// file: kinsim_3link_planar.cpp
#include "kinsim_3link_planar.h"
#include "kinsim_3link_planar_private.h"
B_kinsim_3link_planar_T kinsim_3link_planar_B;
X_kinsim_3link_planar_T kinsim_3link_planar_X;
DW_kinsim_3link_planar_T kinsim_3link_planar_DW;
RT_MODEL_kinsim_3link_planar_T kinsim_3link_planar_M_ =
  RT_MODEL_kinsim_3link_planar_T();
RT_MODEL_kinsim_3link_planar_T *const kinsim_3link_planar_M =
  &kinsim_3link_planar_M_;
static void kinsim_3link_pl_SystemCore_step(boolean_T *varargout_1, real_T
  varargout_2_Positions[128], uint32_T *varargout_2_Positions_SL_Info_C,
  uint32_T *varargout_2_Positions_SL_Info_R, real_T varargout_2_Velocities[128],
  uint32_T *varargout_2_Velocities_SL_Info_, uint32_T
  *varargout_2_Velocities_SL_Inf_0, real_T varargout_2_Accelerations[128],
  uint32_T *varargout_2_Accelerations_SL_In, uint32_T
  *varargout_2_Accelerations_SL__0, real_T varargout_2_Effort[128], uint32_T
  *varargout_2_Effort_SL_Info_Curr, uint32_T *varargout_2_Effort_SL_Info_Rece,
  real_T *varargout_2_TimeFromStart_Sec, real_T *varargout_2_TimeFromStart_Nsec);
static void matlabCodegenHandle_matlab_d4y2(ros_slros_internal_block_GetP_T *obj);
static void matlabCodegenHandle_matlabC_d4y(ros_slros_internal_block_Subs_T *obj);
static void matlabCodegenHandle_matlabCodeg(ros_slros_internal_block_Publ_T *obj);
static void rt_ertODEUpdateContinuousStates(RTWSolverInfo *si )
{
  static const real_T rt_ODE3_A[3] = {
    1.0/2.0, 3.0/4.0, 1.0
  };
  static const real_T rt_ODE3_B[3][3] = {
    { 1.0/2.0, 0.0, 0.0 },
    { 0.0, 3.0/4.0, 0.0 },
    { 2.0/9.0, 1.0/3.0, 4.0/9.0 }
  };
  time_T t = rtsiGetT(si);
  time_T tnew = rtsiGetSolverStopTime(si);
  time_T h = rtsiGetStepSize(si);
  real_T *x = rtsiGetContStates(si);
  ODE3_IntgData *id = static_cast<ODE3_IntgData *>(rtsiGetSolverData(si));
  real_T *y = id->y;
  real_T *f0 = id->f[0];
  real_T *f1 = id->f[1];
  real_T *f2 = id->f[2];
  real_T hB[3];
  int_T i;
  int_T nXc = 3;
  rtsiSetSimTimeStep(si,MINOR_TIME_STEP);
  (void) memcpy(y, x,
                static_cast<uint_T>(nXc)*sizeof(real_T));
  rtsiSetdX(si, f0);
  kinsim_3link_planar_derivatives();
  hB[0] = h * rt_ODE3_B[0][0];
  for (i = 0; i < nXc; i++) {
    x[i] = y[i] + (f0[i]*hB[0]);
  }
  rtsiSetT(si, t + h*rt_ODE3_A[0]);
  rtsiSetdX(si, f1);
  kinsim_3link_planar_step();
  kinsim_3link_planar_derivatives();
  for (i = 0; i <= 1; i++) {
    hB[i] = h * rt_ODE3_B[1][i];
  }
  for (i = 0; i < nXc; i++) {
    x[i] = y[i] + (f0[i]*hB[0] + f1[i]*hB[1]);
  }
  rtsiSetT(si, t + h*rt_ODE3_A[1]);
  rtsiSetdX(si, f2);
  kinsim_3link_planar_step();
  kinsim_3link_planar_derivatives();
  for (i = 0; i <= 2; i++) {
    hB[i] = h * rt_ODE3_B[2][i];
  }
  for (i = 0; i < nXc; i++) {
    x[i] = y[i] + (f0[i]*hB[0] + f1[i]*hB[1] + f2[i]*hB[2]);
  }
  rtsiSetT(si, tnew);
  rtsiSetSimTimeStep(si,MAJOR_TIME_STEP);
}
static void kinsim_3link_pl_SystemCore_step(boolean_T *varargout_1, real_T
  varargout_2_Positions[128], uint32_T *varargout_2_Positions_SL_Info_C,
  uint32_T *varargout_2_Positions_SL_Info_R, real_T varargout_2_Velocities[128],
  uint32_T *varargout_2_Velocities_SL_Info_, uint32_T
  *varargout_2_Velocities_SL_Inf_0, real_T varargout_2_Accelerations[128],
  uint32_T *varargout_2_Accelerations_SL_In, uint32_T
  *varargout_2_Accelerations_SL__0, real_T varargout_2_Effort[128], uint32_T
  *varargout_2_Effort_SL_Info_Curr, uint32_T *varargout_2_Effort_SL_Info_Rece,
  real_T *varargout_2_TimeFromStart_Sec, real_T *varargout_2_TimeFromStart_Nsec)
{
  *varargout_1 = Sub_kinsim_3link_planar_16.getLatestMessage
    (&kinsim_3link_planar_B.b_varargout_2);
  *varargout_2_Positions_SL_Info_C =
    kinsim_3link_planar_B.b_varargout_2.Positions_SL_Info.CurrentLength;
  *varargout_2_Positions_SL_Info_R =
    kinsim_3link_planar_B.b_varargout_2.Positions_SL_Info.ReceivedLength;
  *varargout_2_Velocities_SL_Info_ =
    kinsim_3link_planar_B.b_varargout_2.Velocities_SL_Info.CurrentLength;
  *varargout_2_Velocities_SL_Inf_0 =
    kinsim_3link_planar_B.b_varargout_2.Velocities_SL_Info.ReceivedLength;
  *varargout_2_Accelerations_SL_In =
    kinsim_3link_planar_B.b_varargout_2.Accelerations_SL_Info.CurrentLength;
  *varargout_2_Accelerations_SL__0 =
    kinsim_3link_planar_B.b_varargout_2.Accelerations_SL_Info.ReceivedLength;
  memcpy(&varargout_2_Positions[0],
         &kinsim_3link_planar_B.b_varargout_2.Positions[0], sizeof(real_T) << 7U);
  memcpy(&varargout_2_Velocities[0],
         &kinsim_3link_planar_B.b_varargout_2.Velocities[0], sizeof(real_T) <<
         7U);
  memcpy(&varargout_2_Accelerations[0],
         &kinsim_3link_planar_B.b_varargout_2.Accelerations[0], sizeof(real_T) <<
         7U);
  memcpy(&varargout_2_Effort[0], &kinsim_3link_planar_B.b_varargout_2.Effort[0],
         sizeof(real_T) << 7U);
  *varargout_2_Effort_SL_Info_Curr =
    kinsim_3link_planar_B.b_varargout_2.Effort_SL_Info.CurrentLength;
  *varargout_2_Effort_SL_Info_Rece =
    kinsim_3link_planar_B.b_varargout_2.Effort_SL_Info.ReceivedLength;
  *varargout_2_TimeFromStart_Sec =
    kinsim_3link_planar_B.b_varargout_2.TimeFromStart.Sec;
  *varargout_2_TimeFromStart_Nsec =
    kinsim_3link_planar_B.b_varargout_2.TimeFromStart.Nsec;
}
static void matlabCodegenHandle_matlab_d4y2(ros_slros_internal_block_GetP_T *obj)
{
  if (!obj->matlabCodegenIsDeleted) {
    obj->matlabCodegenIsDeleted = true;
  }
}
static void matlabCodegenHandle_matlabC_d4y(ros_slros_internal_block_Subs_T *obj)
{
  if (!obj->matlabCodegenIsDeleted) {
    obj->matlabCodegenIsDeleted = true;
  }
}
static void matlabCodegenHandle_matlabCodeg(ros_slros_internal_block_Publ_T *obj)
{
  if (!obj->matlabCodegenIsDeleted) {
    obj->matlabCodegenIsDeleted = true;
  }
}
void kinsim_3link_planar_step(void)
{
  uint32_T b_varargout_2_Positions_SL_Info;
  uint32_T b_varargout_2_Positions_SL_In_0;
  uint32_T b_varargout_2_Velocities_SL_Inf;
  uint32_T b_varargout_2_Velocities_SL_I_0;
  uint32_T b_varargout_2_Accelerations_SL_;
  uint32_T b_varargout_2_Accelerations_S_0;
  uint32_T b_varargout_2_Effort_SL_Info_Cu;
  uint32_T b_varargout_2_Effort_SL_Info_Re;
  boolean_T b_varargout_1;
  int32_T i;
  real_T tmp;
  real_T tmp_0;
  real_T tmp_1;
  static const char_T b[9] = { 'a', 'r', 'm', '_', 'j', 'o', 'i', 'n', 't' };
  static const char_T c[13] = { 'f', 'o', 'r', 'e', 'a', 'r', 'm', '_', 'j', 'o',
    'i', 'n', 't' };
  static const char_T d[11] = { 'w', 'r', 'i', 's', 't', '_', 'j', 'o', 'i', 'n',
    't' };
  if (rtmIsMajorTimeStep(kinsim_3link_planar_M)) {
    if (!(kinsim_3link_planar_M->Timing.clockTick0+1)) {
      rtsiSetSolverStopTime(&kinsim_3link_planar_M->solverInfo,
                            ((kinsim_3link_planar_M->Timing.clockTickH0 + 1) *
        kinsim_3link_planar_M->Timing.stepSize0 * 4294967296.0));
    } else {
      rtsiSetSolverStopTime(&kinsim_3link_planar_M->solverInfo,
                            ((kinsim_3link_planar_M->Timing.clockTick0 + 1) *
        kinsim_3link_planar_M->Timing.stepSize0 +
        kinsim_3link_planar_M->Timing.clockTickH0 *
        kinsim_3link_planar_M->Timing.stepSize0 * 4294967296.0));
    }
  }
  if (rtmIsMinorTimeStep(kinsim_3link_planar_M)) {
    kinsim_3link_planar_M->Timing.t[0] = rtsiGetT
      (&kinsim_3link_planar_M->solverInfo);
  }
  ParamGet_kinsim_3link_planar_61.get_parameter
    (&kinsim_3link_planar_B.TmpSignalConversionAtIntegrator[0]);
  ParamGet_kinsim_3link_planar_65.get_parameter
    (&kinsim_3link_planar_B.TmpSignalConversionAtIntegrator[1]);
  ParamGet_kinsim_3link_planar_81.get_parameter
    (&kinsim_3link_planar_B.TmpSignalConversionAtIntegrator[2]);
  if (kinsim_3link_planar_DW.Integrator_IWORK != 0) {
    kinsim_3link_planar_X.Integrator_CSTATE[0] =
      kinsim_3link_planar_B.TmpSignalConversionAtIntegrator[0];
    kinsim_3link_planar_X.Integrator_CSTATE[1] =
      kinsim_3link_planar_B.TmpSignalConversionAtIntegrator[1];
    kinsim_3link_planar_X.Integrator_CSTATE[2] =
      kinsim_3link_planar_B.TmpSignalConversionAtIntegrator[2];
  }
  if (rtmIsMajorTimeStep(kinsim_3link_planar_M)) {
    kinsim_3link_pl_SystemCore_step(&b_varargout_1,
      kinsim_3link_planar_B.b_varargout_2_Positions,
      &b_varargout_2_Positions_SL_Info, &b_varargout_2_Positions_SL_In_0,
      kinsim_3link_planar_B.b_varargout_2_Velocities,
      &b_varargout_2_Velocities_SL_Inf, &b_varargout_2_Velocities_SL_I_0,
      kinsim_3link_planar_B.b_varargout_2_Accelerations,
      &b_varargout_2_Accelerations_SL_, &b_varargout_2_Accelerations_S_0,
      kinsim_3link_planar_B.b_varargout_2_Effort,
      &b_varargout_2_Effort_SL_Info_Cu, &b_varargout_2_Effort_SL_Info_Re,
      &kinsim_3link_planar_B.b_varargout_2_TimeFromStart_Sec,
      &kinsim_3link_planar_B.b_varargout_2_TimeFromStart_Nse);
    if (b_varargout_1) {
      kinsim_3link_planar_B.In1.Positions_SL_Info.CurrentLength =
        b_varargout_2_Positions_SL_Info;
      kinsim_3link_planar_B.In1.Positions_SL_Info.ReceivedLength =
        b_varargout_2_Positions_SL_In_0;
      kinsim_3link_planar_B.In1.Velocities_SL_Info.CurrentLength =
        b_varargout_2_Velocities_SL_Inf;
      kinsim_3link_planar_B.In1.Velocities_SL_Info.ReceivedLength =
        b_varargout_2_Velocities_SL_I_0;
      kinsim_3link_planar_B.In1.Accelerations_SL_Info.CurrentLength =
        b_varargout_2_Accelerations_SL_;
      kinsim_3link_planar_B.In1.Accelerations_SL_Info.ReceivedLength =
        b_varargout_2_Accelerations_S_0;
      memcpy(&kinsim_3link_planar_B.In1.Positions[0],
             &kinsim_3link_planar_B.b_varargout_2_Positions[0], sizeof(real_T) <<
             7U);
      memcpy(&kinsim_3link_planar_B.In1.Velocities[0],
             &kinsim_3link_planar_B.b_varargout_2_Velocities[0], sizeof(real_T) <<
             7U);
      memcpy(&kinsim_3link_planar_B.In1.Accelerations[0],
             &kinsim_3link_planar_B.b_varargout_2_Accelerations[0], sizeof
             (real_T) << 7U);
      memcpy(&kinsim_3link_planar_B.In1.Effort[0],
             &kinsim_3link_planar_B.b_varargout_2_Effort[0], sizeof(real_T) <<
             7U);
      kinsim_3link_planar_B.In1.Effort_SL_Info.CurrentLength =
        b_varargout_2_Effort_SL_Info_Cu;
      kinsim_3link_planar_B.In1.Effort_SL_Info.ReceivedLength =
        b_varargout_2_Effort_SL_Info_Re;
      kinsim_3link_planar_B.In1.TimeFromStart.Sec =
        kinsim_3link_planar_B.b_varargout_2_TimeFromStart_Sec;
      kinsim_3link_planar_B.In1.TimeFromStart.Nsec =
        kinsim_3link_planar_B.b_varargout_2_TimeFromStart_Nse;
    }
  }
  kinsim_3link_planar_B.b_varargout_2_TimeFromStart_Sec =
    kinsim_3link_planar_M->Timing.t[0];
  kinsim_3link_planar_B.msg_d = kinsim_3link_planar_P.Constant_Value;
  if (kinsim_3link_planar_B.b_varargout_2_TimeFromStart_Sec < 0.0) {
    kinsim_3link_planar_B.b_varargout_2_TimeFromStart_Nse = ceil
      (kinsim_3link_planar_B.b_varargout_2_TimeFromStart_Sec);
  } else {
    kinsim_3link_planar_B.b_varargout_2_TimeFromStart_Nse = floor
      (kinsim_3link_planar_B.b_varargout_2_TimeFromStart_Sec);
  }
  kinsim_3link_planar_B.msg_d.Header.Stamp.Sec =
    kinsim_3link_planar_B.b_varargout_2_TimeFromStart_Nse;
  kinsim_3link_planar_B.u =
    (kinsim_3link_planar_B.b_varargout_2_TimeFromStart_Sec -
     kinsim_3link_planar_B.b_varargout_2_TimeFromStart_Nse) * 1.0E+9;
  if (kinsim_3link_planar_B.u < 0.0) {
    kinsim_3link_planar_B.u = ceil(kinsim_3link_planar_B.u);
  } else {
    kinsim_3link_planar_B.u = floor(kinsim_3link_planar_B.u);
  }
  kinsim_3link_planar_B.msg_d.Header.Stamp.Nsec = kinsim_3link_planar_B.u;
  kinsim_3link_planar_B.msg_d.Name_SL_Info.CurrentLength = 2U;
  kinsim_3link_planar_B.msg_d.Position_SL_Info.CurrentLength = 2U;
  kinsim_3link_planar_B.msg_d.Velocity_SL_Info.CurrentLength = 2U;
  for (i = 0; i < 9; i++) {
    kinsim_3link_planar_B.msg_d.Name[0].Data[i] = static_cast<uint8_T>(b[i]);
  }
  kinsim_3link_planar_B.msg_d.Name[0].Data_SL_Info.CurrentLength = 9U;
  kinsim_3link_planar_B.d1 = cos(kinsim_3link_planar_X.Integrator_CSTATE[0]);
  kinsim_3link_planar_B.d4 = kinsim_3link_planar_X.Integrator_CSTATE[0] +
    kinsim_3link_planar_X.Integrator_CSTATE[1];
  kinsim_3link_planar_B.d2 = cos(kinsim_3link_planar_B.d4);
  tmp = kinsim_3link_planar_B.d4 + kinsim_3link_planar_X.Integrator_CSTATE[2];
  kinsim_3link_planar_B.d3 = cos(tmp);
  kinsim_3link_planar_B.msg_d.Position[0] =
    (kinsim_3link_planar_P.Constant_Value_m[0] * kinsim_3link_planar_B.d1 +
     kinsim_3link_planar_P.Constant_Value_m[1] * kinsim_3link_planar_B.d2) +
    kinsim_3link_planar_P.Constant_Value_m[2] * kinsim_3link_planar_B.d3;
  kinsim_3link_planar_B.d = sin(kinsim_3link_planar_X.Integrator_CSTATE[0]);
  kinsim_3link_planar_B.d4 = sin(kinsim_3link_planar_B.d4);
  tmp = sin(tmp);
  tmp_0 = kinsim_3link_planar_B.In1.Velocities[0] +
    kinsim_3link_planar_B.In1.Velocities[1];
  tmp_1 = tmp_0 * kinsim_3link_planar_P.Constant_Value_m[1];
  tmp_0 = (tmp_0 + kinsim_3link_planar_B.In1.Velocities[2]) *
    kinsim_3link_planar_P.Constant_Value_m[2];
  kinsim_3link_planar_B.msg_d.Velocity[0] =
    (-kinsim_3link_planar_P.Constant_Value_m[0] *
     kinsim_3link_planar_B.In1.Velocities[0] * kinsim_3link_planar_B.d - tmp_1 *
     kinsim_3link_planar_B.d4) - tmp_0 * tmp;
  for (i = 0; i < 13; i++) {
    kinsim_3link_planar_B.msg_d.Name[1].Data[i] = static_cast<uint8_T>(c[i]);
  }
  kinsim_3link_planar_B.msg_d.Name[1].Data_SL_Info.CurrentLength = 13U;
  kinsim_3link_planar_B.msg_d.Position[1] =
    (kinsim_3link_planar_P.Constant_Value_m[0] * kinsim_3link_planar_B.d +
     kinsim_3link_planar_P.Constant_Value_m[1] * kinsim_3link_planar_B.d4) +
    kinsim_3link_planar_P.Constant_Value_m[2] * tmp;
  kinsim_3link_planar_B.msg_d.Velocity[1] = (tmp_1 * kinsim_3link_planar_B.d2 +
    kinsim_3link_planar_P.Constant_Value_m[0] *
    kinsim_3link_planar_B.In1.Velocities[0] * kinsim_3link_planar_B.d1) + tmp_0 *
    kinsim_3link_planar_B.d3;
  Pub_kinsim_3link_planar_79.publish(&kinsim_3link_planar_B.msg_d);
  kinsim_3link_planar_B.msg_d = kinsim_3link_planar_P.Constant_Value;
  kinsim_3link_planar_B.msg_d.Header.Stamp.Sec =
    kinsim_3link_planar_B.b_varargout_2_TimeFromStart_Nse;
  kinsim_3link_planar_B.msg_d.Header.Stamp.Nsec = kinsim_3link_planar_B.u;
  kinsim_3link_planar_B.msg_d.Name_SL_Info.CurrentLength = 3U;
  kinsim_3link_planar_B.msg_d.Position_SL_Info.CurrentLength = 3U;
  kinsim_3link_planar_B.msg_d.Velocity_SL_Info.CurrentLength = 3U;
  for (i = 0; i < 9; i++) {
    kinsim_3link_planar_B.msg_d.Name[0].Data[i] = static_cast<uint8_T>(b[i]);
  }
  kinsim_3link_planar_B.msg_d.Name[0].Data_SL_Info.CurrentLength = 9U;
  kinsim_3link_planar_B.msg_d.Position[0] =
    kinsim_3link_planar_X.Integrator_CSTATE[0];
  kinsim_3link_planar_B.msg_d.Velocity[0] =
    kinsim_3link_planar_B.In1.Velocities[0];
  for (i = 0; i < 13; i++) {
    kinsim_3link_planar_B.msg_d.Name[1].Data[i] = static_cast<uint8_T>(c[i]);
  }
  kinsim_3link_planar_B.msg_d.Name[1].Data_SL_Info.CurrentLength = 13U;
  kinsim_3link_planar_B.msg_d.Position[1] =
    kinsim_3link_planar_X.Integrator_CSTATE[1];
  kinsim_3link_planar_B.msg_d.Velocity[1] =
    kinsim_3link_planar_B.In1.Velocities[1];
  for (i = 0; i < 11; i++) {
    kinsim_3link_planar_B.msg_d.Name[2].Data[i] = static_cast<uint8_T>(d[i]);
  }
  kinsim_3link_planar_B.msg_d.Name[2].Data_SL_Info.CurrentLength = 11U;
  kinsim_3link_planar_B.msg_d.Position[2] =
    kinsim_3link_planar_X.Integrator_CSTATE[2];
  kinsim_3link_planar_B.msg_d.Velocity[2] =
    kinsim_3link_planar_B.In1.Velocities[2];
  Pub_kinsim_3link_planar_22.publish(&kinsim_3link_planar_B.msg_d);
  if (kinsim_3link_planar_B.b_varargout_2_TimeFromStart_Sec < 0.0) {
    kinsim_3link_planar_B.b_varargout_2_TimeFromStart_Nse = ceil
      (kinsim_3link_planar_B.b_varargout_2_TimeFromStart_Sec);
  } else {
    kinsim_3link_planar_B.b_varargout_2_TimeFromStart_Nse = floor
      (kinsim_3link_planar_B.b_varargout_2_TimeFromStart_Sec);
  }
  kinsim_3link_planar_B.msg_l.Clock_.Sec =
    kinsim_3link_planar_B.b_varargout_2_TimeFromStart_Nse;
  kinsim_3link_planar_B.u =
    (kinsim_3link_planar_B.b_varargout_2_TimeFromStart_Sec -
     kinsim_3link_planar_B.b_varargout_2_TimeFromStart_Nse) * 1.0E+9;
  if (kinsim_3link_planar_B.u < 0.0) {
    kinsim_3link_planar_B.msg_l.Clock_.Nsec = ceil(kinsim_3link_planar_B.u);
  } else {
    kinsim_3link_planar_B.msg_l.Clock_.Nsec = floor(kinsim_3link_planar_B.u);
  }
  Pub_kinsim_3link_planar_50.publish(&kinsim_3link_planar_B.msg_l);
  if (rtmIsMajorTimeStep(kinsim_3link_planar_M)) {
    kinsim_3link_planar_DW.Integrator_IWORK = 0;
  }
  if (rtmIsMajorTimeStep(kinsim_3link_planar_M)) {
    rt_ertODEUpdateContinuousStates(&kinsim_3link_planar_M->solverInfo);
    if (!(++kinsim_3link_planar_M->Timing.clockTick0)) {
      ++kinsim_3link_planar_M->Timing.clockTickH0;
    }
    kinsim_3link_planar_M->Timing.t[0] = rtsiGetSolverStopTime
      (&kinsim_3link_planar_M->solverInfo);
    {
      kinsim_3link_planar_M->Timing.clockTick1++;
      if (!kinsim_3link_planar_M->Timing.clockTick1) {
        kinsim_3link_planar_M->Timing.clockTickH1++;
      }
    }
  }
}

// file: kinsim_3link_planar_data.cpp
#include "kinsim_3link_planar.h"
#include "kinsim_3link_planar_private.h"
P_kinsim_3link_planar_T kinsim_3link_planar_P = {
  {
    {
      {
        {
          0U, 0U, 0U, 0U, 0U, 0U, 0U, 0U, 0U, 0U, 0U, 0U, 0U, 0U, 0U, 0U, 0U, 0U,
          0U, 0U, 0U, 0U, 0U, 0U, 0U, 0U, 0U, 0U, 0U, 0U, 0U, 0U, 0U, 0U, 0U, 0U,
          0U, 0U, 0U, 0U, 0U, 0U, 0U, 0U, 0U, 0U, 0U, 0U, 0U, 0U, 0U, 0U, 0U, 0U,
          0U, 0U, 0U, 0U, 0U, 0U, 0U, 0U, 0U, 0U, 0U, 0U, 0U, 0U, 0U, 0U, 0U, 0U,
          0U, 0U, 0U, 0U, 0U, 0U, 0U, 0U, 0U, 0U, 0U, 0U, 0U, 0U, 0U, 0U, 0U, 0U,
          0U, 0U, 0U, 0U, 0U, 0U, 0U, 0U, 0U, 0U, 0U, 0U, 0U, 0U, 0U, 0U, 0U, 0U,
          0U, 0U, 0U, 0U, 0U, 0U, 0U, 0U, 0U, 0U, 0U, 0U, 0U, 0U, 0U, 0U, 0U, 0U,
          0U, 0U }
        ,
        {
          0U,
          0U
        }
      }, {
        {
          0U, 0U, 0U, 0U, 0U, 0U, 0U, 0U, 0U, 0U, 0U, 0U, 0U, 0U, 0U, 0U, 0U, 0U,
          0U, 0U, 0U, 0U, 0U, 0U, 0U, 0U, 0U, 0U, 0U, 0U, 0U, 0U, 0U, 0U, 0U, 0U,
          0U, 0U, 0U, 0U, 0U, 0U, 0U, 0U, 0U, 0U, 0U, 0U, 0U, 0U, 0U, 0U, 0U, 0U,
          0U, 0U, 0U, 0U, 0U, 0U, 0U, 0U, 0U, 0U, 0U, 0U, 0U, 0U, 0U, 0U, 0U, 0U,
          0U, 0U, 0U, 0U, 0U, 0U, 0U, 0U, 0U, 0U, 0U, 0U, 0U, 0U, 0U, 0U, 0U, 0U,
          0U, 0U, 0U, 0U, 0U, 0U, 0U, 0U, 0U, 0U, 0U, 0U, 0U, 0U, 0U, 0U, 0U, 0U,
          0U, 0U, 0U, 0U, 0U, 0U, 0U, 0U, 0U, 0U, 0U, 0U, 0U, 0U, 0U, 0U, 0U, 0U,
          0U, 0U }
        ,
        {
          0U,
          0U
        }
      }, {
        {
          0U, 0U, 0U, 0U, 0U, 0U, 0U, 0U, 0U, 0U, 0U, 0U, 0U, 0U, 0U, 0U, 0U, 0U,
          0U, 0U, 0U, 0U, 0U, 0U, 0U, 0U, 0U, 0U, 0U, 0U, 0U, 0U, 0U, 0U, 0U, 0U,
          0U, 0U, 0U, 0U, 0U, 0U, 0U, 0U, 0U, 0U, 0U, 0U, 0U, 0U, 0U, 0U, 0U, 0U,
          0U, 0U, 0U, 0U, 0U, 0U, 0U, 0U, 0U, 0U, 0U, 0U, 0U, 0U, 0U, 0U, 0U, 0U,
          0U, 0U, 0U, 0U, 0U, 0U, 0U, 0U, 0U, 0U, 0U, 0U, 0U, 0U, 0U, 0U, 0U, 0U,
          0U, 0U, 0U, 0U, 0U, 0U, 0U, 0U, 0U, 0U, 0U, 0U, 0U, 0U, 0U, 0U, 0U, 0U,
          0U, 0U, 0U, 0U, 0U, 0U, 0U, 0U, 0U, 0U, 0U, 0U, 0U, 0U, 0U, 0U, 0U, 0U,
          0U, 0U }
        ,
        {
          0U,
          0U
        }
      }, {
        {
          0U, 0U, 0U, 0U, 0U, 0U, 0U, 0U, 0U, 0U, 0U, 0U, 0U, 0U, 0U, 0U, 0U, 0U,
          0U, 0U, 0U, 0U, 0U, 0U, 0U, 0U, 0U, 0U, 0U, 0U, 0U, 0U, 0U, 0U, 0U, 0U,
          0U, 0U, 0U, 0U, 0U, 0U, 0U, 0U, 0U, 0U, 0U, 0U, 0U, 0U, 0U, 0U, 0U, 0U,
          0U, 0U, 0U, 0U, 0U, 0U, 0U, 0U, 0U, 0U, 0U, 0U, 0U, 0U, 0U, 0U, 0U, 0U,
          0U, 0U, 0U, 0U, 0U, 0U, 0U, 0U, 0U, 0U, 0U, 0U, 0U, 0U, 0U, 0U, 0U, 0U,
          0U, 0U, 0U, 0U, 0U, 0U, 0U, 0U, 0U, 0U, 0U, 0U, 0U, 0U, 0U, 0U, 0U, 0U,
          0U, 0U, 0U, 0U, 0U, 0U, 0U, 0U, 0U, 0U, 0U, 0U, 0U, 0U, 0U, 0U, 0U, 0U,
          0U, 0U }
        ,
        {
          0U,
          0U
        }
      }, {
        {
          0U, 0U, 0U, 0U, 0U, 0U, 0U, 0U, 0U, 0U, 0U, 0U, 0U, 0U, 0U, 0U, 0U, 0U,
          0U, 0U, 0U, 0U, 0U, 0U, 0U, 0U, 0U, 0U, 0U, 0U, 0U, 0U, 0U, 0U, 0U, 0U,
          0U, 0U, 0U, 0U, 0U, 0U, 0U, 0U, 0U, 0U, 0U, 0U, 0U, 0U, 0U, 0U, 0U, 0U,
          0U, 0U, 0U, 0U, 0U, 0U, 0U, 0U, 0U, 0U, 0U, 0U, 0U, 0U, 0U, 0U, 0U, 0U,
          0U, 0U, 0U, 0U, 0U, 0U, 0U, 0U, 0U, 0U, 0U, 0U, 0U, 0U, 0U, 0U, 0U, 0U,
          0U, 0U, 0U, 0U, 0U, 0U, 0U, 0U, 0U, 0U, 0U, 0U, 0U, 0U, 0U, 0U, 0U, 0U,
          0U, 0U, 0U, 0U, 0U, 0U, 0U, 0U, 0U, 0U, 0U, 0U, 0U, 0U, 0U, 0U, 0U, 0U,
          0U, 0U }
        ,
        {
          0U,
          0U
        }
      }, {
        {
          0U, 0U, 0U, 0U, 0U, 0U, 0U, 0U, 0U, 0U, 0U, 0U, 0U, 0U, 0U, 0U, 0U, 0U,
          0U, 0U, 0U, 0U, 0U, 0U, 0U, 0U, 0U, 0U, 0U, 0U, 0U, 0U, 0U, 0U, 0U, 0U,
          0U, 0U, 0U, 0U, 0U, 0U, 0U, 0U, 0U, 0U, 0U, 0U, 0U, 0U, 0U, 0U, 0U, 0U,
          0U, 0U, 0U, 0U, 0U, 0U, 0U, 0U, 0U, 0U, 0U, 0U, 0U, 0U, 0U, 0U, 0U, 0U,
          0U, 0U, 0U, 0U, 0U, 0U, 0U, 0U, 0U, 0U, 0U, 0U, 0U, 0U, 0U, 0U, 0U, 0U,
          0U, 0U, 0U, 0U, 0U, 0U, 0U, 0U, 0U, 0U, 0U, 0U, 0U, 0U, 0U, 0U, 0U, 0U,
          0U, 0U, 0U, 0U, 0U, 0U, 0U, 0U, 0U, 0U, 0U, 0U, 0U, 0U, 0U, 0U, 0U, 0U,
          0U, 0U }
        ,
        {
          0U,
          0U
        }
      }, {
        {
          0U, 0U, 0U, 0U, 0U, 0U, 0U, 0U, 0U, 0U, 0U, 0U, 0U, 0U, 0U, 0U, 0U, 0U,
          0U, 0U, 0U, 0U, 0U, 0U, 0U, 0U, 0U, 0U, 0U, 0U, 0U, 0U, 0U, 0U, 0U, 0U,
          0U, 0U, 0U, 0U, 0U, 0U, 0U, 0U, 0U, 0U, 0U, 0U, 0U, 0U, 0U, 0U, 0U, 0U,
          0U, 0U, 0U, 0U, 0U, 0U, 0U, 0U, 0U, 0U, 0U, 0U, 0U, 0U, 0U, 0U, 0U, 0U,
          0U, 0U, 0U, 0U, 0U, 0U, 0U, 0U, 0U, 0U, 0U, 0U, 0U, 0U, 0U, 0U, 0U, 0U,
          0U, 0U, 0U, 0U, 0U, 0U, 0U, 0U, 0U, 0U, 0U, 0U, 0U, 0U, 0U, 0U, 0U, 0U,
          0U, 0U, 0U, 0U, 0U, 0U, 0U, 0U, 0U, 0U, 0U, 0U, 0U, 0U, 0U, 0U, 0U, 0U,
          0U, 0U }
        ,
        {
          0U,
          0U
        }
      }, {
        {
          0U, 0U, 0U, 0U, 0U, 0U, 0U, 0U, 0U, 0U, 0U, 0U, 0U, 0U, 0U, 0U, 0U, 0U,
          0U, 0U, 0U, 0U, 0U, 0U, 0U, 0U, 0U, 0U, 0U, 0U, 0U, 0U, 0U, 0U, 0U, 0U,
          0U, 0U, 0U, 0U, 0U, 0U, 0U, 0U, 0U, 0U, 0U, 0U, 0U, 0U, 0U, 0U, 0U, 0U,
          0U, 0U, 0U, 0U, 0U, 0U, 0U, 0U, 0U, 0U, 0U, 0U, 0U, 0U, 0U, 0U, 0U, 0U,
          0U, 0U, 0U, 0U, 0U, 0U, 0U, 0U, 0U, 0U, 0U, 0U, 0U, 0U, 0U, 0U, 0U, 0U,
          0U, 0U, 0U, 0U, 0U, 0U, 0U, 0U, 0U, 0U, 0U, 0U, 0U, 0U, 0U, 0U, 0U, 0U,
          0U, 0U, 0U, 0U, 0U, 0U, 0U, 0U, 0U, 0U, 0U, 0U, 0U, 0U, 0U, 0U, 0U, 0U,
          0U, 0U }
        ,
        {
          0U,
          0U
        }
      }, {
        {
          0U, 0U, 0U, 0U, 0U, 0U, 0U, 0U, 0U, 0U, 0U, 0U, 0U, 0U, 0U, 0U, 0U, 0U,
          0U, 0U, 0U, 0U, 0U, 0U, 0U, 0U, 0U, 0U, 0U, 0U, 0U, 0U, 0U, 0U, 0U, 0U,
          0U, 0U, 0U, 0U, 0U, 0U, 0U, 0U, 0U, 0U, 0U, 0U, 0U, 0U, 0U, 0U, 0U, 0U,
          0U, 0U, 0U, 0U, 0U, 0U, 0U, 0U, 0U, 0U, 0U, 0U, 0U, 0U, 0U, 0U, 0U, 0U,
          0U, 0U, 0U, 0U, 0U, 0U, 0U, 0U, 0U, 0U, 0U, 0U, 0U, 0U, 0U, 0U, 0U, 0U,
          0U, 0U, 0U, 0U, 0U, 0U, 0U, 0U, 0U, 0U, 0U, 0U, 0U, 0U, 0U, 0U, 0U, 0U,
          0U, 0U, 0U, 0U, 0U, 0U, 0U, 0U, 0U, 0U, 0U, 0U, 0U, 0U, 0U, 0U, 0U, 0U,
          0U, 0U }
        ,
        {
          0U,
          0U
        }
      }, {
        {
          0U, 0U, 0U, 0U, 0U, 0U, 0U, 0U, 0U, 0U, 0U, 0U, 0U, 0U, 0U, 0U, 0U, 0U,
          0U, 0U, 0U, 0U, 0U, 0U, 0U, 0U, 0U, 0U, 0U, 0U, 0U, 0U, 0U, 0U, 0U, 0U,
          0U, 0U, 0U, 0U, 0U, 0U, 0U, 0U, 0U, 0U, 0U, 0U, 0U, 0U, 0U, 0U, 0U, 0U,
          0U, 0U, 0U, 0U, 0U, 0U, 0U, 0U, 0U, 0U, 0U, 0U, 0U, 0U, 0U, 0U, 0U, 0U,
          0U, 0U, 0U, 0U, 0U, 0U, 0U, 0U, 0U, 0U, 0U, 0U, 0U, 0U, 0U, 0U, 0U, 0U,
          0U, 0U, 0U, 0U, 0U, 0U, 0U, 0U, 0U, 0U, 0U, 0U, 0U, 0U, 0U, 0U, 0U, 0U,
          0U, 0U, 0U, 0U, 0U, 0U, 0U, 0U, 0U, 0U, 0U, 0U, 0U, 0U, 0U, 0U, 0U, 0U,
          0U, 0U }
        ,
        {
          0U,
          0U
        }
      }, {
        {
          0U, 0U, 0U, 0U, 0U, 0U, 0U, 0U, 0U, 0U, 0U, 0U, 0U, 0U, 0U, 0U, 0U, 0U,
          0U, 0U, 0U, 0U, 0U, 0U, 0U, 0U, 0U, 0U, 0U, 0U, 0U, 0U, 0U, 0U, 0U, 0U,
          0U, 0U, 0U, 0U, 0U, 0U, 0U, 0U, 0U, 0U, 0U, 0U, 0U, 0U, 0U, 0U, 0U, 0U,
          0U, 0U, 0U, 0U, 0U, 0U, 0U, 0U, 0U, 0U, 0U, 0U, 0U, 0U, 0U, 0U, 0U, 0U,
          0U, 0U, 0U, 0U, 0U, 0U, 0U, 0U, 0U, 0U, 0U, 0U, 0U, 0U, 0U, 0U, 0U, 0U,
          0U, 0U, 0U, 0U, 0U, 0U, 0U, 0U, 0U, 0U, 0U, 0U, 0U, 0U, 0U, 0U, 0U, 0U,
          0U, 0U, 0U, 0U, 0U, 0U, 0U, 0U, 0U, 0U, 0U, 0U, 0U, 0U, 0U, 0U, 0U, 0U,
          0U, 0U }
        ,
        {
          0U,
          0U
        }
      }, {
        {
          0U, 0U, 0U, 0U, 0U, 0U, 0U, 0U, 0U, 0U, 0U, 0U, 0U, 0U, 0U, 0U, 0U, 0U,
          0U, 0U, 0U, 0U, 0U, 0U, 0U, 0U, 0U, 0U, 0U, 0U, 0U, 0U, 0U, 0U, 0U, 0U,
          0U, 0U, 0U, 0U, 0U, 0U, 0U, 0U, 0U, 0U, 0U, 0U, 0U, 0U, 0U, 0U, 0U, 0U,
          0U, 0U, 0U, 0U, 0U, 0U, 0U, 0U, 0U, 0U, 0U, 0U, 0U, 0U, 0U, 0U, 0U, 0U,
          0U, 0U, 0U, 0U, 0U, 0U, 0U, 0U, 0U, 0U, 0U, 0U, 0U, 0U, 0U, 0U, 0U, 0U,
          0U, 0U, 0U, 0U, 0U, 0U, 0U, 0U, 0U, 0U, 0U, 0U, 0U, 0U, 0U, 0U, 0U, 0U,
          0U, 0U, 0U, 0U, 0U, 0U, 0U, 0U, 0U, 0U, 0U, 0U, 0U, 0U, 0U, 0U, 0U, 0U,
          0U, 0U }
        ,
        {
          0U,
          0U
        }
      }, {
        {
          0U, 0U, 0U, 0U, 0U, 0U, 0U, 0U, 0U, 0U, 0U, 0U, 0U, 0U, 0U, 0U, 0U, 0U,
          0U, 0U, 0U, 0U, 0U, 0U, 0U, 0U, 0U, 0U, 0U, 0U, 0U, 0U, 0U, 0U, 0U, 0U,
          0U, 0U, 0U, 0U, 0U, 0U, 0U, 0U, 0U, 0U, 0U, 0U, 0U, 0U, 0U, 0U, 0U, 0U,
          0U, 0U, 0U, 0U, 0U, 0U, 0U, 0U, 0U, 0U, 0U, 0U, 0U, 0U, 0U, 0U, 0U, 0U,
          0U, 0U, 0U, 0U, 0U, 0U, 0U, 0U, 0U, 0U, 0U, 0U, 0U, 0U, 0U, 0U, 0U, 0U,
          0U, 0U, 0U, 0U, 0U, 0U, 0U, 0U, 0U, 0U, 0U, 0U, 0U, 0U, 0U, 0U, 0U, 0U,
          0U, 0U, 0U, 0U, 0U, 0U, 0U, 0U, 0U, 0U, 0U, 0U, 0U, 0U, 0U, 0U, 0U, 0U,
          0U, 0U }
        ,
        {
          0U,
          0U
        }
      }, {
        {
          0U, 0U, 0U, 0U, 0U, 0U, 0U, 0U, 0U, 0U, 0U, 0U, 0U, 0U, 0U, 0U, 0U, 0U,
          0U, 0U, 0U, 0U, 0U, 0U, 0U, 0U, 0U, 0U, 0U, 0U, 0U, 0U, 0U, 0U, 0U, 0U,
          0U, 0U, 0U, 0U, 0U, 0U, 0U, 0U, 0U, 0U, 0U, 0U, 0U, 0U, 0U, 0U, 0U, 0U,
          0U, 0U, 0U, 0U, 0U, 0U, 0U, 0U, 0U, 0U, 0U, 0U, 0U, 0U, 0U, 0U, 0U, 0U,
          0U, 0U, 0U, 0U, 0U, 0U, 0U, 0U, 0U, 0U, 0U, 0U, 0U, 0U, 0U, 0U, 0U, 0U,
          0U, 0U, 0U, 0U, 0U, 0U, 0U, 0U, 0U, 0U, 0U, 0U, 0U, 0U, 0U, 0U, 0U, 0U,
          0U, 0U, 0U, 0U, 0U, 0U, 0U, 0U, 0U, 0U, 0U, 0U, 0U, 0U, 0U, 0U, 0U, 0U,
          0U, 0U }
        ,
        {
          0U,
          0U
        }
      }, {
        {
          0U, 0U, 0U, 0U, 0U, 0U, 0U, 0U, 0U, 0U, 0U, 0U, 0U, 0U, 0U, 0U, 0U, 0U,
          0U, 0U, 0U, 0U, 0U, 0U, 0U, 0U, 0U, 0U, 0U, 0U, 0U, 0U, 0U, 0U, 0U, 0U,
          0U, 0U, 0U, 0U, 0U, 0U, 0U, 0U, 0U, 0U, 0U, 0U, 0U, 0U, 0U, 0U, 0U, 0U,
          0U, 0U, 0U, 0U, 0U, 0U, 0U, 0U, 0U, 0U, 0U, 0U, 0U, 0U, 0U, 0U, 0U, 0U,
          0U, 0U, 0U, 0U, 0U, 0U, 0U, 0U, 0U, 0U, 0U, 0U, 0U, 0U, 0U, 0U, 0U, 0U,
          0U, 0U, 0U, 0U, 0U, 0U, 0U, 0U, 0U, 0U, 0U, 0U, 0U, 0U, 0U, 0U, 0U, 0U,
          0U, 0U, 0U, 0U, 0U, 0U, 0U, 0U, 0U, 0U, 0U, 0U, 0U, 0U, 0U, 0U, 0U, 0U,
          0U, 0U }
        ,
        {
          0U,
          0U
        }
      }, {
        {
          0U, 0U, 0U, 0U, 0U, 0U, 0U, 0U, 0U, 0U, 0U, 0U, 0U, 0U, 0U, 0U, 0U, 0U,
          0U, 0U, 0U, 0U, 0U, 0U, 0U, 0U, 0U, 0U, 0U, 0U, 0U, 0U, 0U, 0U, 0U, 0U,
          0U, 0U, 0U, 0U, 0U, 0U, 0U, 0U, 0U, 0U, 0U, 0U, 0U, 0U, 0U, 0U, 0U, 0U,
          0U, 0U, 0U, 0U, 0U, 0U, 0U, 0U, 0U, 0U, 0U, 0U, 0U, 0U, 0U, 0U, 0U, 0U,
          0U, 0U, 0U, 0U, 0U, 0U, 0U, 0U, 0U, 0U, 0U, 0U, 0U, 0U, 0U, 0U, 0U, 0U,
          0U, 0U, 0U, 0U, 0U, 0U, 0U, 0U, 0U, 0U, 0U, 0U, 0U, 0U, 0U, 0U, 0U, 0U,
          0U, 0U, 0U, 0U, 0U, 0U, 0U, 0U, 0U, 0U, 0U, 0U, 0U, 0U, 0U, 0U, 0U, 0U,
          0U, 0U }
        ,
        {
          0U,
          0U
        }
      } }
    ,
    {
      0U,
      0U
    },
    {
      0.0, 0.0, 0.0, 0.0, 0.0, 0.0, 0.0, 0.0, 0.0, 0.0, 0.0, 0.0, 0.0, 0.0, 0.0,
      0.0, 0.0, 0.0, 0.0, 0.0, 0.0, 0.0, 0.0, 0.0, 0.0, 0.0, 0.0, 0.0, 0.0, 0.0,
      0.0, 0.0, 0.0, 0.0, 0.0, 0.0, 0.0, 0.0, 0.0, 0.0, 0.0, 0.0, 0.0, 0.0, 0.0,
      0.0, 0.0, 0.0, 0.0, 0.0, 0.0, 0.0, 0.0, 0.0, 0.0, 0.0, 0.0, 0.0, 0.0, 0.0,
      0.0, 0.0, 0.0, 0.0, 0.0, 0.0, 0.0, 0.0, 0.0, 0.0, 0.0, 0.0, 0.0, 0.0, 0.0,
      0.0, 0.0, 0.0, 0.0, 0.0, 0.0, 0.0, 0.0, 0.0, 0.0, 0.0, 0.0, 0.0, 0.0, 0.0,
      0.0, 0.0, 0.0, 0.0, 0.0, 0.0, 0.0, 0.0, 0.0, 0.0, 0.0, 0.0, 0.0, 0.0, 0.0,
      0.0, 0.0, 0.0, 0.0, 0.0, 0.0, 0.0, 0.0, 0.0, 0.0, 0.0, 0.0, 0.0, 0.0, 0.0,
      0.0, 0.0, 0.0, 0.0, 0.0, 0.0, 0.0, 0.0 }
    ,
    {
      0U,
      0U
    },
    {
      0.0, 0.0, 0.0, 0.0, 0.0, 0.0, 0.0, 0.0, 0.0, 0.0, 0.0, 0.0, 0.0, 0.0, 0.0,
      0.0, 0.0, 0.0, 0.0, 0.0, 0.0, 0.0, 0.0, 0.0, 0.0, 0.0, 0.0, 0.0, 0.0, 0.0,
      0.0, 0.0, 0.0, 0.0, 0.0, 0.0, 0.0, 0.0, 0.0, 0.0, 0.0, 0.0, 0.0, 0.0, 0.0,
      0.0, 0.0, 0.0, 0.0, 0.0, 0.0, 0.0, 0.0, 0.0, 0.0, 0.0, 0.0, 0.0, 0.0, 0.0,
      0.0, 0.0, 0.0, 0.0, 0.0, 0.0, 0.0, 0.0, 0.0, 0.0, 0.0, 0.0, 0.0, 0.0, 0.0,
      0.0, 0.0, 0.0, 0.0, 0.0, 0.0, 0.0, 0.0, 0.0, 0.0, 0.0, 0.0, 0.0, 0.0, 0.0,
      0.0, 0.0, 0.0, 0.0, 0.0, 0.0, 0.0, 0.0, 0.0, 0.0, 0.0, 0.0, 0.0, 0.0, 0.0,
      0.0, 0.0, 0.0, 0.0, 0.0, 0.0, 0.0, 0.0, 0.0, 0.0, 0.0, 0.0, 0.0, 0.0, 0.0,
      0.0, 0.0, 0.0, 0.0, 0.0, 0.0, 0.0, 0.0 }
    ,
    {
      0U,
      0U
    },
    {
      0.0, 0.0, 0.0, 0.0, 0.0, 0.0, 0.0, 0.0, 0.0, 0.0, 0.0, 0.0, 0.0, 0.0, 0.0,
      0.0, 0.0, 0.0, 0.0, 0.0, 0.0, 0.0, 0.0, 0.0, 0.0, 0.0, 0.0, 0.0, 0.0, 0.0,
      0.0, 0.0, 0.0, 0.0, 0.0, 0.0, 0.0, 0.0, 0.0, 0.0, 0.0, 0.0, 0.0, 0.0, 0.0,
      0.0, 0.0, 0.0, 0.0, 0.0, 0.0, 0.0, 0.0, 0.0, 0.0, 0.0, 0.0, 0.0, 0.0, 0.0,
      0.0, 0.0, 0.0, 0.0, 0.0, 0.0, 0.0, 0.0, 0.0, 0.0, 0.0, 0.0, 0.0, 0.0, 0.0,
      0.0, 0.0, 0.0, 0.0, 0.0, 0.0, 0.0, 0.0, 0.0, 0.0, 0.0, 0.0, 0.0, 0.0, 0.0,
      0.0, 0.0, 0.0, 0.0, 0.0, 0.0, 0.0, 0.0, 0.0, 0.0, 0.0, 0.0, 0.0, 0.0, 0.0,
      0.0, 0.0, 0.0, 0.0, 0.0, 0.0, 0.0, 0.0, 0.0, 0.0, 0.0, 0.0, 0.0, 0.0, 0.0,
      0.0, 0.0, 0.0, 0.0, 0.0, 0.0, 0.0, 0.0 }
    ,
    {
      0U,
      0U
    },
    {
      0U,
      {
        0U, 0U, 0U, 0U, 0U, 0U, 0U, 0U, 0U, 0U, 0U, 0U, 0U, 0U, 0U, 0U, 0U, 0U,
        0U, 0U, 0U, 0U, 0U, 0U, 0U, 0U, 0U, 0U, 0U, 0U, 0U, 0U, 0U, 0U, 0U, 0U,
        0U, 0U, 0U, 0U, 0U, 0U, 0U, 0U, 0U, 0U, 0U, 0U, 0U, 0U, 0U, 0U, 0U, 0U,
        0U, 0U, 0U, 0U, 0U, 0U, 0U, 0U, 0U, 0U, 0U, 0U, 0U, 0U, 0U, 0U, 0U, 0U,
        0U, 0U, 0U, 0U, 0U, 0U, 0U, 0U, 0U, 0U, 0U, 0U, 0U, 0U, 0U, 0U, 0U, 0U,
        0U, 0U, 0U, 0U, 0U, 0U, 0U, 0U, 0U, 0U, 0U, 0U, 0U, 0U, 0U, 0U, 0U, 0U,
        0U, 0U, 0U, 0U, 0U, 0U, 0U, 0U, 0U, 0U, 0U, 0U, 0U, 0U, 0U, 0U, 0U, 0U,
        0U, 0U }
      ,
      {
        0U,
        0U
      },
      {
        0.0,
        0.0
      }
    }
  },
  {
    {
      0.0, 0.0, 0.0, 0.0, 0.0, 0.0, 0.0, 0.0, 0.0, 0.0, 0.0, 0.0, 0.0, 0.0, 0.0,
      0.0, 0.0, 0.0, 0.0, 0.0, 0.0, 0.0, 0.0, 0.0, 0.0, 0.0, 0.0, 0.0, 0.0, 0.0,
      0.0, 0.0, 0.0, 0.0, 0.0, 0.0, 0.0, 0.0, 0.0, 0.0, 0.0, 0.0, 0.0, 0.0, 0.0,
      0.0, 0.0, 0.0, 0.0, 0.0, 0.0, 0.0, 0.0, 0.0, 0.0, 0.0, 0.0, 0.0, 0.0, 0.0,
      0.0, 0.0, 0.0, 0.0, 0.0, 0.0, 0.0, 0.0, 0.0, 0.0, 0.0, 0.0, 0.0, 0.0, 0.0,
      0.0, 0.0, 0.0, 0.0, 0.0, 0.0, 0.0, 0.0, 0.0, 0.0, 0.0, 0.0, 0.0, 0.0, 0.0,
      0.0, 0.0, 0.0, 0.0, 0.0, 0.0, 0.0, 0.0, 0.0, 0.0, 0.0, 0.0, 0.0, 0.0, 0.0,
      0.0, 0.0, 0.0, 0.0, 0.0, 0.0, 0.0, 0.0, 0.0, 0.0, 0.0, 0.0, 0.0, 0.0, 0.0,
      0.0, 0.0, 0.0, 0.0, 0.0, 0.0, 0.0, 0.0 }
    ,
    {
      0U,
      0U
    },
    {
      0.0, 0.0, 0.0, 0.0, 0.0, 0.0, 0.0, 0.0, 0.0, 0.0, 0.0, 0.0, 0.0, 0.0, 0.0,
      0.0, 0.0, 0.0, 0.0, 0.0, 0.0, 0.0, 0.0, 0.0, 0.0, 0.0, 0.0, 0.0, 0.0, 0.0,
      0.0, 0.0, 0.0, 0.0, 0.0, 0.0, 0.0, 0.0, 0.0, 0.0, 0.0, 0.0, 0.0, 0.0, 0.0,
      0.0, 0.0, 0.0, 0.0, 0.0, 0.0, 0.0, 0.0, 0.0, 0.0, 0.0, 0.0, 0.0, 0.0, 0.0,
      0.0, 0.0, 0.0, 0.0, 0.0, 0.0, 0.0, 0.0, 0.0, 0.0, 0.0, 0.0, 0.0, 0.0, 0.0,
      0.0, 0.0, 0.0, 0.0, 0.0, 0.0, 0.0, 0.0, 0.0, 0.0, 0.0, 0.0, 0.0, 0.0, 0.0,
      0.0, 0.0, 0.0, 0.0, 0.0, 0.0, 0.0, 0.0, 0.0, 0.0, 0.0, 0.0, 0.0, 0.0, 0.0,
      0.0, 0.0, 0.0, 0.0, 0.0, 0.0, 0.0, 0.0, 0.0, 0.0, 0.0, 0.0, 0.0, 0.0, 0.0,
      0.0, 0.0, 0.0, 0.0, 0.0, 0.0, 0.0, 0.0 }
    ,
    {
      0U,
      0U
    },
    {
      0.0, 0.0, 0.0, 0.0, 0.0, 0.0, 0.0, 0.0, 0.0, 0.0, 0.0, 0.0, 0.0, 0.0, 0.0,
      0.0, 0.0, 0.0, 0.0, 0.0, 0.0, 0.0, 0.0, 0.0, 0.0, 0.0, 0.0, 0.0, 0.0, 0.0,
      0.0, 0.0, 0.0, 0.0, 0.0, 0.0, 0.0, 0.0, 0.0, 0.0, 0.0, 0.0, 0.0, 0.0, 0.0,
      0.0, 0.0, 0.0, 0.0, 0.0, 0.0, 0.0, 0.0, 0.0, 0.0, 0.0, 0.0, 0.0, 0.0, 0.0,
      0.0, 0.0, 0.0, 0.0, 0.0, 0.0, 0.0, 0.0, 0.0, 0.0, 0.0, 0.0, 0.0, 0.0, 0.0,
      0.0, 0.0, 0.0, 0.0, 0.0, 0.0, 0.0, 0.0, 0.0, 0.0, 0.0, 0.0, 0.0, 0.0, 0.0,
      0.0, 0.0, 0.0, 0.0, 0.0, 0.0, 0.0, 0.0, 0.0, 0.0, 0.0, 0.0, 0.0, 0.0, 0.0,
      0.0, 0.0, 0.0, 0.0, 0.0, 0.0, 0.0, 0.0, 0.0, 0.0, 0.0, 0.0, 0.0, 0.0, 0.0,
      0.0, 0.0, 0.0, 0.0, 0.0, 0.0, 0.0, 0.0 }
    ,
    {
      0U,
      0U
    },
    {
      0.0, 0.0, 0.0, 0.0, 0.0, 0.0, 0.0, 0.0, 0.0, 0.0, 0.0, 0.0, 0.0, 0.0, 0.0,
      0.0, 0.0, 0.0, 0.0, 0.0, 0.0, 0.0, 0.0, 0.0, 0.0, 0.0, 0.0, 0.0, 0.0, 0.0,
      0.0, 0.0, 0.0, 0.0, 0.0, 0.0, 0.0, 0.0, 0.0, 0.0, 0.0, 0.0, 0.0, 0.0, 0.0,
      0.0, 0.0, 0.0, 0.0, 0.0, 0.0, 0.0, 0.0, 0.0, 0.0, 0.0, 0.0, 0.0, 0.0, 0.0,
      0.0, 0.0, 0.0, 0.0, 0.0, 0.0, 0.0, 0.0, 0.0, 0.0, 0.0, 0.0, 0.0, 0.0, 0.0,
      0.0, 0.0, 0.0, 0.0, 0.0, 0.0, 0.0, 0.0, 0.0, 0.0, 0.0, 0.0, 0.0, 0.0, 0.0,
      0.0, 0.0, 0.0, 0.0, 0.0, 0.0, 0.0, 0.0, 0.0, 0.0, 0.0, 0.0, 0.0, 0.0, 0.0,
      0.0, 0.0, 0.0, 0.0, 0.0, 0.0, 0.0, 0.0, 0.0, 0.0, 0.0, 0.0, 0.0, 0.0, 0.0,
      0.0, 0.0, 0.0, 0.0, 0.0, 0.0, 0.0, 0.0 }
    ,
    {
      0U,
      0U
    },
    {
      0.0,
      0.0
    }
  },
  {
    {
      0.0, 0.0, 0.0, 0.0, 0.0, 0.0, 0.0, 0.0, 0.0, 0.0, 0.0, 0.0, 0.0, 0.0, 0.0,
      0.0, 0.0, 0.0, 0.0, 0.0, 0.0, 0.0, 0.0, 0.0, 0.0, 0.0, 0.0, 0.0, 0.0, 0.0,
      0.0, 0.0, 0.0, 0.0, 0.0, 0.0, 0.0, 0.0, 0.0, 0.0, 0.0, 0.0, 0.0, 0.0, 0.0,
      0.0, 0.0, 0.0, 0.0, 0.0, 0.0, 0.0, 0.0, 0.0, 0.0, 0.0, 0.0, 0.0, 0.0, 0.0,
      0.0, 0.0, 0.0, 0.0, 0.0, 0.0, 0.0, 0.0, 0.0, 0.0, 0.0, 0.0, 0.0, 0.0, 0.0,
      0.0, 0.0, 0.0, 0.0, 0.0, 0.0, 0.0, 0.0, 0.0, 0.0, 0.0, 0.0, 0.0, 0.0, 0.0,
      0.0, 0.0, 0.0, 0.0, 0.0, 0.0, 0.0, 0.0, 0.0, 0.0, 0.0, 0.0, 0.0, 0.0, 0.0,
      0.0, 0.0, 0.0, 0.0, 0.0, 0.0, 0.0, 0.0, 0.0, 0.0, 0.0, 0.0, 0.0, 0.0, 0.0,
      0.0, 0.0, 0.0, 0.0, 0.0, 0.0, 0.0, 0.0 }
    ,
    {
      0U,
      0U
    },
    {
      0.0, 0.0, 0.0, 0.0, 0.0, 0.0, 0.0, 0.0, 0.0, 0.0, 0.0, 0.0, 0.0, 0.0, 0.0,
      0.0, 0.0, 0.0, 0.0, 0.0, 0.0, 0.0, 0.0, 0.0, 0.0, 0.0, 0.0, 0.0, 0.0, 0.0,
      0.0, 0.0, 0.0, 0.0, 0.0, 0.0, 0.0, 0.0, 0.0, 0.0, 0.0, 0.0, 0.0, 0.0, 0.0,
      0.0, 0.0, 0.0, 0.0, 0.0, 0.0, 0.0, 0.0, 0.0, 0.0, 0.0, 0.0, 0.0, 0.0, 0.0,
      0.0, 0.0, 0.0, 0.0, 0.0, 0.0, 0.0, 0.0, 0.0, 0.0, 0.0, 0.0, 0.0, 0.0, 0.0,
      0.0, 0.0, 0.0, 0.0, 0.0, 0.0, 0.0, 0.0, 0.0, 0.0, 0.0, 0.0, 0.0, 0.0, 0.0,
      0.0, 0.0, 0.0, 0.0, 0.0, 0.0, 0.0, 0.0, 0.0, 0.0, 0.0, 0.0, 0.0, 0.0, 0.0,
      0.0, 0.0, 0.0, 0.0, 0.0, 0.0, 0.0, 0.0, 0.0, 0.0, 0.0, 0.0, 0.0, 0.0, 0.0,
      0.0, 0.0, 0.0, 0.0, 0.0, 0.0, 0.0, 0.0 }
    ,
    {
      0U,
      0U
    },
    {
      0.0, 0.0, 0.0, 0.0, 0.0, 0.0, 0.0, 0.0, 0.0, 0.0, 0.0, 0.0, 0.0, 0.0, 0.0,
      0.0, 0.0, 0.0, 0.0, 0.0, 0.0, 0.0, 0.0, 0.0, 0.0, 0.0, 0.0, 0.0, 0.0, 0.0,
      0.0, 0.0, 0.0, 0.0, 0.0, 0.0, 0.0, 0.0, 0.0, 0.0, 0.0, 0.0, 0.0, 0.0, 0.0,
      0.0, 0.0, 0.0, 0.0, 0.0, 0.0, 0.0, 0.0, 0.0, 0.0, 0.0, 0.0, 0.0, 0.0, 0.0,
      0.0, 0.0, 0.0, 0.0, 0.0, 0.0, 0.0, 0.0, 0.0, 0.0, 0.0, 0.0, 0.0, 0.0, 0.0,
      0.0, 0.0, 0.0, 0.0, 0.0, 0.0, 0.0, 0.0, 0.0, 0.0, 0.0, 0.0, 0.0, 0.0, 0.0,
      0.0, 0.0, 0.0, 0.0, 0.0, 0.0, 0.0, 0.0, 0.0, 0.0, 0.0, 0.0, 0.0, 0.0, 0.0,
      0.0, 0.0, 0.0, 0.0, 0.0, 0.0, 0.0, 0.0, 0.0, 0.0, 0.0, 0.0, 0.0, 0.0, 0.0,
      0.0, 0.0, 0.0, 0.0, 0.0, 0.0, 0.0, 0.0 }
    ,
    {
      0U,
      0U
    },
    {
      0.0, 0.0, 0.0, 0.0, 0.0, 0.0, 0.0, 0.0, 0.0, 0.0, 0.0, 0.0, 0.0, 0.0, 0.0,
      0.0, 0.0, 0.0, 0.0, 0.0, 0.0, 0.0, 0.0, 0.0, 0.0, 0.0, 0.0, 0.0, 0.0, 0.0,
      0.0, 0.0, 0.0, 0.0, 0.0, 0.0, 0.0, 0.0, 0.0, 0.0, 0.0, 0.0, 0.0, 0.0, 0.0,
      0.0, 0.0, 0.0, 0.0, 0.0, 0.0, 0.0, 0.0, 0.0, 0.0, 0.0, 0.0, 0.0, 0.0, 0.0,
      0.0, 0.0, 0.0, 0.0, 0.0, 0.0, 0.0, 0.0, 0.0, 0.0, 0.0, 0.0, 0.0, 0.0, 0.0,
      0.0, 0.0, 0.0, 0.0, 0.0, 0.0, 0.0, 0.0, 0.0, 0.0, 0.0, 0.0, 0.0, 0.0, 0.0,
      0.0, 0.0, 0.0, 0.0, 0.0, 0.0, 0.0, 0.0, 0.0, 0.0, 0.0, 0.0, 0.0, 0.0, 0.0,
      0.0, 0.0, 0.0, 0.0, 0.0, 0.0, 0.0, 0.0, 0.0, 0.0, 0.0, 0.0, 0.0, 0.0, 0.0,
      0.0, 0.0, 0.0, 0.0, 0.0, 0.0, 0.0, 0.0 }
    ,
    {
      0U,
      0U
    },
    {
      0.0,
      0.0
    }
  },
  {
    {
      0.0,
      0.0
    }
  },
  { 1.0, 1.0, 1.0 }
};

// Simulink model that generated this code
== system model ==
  Publish#1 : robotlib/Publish  <- 1: MATLABFunction#1
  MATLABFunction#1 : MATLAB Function  <- 1: BlankMessage#1, 2: MATLABFunction#2, 3: MATLABFunction#2/2, 4: Clock#1
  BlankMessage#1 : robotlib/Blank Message
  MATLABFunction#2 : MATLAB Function  <- 1: Integrator, 2: Selector#1, 3: Constant
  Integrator : Integrator  InitialCondition=[0,0]  <- 1: Selector#1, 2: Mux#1
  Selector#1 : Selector  Indices=[1]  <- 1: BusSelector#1
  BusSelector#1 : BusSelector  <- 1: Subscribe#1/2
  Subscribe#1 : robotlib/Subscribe
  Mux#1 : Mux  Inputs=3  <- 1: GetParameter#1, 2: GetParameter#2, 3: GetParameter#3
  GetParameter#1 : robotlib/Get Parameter
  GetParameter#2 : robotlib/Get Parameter
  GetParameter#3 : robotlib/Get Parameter
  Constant : Constant  Value=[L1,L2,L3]
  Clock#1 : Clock
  Publish#2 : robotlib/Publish  <- 1: MATLABFunction#3
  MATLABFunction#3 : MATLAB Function  <- 1: BlankMessage#1, 2: Integrator, 3: Selector#1, 4: Clock#1
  Publish#3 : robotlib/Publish  <- 1: MATLABFunction#4
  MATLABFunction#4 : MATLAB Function  <- 1: BlankMessage#2, 2: Clock
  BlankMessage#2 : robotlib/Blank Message
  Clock : Clock
== matlab function MATLABFunction#4 ==
function msg = assign_Time(blankMessage,time)
%#codegen

% Assign the output message to be the same with input blank message
msg = blankMessage;

% Convert and set time
msg.Clock_.Sec  = fix(time);
msg.Clock_.Nsec = fix((time-fix(time))*1e9);

== matlab function MATLABFunction#3 ==
function msg = assign_JointState(blankMessage,jointPos,jointVel,time)
%#codegen

% Assign the output message to be the same with input blank message
msg = blankMessage;

% Initialize time stamp
msg.Header.Stamp.Sec  = fix(time);
msg.Header.Stamp.Nsec = fix((time-fix(time))*1e9);

% Set the number of strings in the string array, and joint positions/velocities in the position/velocity array
numJoints = length(jointPos);
msg.Name_SL_Info.CurrentLength = uint32(numJoints);
msg.Position_SL_Info.CurrentLength = uint32(numJoints);
msg.Velocity_SL_Info.CurrentLength = uint32(numJoints);

% Set the individual components in the message arrays
strArrayToAssign = {'arm_joint', 'forearm_joint', 'wrist_joint'};

for idx=1:numJoints
    str = strArrayToAssign{idx};
    strLength = length(str);
    msg.Name(idx).Data(1:strLength) = uint8(str);
    msg.Name(idx).Data_SL_Info.CurrentLength = uint32(strLength);

    msg.Position(idx) = jointPos(idx);
    msg.Velocity(idx) = jointVel(idx);
end

== matlab function MATLABFunction#2 ==
function [cartPos, cartVel] = forward_kinematics_3link(jointPos,jointVel,linkLength)

cartPos = zeros(1,2);
cartVel = zeros(1,2);

L1 = linkLength(1);
L2 = linkLength(2);
L3 = linkLength(3);
q1 = jointPos(1);
q2 = jointPos(2);
q3 = jointPos(3);
qv1 = jointVel(1);
qv2 = jointVel(2);
qv3 = jointVel(3);

cartPos(1) = L1*cos(q1)+L2*cos(q1+q2)+L3*cos(q1+q2+q3);
cartPos(2) = L1*sin(q1)+L2*sin(q1+q2)+L3*sin(q1+q2+q3);
cartVel(1) = -L1*qv1*sin(q1)-L2*(qv1+qv2)*sin(q1+q2)-L3*(qv1+qv2+qv3)*sin(q1+q2+q3);
cartVel(2) = L1*qv1*cos(q1)+L2*(qv1+qv2)*cos(q1+q2)+L3*(qv1+qv2+qv3)*cos(q1+q2+q3);

== matlab function MATLABFunction#1 ==
function msg = assign_CartesianState(blankMessage,cartPos,cartVel,time)
%#codegen

% Assign the output message to be the same with input blank message
msg = blankMessage;

% Initialize time stamp
msg.Header.Stamp.Sec  = fix(time);
msg.Header.Stamp.Nsec = fix((time-fix(time))*1e9);

% Set the number of strings in the string array, and joint positions/velocities in the position/velocity array
numCoordinates = length(cartPos);
msg.Name_SL_Info.CurrentLength = uint32(numCoordinates);
msg.Position_SL_Info.CurrentLength = uint32(numCoordinates);
msg.Velocity_SL_Info.CurrentLength = uint32(numCoordinates);

% Set the individual components in the message arrays
strArrayToAssign = {'arm_joint', 'forearm_joint', 'wrist_joint'};

for idx=1:numCoordinates
    str = strArrayToAssign{idx};
    strLength = length(str);
    msg.Name(idx).Data(1:strLength) = uint8(str);
    msg.Name(idx).Data_SL_Info.CurrentLength = uint32(strLength);

    msg.Position(idx) = cartPos(idx);
    msg.Velocity(idx) = cartVel(idx);
end
